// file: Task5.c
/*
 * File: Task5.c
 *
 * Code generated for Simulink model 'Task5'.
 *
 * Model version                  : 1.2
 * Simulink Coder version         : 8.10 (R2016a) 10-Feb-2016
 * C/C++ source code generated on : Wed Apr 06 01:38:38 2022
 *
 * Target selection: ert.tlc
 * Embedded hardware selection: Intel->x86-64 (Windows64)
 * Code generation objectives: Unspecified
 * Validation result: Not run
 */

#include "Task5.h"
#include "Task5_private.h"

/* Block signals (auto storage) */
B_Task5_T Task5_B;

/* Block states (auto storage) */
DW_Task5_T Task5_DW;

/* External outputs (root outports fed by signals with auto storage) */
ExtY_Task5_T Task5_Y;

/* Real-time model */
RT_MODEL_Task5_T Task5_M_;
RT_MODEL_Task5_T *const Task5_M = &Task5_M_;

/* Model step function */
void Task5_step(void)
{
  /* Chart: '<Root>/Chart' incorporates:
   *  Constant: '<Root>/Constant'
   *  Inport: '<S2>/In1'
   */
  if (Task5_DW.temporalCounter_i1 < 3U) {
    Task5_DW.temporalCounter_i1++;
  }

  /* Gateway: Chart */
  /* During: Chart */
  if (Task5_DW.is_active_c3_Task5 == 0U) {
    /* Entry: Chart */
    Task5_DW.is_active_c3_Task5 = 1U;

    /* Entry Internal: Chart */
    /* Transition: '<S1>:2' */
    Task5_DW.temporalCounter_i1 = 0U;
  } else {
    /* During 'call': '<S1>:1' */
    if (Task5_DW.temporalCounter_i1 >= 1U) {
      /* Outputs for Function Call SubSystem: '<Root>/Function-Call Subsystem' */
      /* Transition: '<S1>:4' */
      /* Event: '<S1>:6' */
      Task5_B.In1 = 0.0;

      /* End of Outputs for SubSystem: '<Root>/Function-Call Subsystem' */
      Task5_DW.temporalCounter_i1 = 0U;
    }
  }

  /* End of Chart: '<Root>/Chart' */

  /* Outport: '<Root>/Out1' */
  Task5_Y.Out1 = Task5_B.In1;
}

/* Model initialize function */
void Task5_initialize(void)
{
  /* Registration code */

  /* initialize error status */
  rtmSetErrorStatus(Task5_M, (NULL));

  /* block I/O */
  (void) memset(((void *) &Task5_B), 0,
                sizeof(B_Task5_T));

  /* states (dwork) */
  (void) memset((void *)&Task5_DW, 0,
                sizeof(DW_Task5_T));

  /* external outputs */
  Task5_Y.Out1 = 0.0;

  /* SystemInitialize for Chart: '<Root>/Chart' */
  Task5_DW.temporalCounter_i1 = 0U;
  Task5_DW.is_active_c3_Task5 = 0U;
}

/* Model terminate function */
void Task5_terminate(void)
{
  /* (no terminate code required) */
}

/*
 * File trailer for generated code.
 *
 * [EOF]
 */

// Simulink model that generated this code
simulink model "Task5"  (R2016a)
settings: Solver=FixedStepDiscrete  StartTime=0.0  StopTime=inf  RelTol=1e-3

== system Task5 ==
  Chart : Stateflow chart  TreatAsAtomicUnit=on
  Constant : Constant  Value=0
  Function-Call Subsystem : Subsystem  TreatAsAtomicUnit=on
  Lamp : Subsystem  DialogController=hmiCreateDDGDialog  IsWebBlock=on  mask(MWDashboardBlock){webBlockId=270aa6e6-eb5d-44ed-ba05-3a2a4bedc3bd, webBlockType=lamp, ShowInLibBrowser=on, ShowInitialText=on, HMISrcModelName=Task5}
      mask prompts: webBlockType "WebBlock Type"; HMISrcModelName "Source Model"
  Toggle Switch : Subsystem  DialogController=hmiCreateDDGDialog  IsWebBlock=on  mask(MWDashboardBlock){webBlockId=34ae164b-30eb-458c-a26c-2fce5357cef7, webBlockType=toggleswitch, ShowInLibBrowser=on, ShowInitialText=on, HMISrcModelName=Task5}
      mask prompts: webBlockId "WebBlock Id"; webBlockType "WebBlock Type"; HMISrcModelName "Source Model"
  Out1 : Outport
  wires:
  Function-Call Subsystem/1(Out1) -> Out1/1
  Constant/1 -> Function-Call Subsystem/1(In1)
  Chart/1(callfunc()) -> Function-Call Subsystem/Trigger

== system Task5/Function-Call Subsystem ==
  In1 : Inport
  function : TriggerPort  TriggerType=function-call  VariantControl=Variant
  Out1 : Outport
  wires:
  In1/1 -> Out1/1

== system Task5/Lamp ==

== system Task5/Toggle Switch ==

== stateflow chart Task5/Chart ==
  state call
    en:
    du:
    ex:
  (default) -> call
  call -> call : [after(5,msec)]{callfunc;}
  events: callfunc output FUNCTION_CALL_EVENT
